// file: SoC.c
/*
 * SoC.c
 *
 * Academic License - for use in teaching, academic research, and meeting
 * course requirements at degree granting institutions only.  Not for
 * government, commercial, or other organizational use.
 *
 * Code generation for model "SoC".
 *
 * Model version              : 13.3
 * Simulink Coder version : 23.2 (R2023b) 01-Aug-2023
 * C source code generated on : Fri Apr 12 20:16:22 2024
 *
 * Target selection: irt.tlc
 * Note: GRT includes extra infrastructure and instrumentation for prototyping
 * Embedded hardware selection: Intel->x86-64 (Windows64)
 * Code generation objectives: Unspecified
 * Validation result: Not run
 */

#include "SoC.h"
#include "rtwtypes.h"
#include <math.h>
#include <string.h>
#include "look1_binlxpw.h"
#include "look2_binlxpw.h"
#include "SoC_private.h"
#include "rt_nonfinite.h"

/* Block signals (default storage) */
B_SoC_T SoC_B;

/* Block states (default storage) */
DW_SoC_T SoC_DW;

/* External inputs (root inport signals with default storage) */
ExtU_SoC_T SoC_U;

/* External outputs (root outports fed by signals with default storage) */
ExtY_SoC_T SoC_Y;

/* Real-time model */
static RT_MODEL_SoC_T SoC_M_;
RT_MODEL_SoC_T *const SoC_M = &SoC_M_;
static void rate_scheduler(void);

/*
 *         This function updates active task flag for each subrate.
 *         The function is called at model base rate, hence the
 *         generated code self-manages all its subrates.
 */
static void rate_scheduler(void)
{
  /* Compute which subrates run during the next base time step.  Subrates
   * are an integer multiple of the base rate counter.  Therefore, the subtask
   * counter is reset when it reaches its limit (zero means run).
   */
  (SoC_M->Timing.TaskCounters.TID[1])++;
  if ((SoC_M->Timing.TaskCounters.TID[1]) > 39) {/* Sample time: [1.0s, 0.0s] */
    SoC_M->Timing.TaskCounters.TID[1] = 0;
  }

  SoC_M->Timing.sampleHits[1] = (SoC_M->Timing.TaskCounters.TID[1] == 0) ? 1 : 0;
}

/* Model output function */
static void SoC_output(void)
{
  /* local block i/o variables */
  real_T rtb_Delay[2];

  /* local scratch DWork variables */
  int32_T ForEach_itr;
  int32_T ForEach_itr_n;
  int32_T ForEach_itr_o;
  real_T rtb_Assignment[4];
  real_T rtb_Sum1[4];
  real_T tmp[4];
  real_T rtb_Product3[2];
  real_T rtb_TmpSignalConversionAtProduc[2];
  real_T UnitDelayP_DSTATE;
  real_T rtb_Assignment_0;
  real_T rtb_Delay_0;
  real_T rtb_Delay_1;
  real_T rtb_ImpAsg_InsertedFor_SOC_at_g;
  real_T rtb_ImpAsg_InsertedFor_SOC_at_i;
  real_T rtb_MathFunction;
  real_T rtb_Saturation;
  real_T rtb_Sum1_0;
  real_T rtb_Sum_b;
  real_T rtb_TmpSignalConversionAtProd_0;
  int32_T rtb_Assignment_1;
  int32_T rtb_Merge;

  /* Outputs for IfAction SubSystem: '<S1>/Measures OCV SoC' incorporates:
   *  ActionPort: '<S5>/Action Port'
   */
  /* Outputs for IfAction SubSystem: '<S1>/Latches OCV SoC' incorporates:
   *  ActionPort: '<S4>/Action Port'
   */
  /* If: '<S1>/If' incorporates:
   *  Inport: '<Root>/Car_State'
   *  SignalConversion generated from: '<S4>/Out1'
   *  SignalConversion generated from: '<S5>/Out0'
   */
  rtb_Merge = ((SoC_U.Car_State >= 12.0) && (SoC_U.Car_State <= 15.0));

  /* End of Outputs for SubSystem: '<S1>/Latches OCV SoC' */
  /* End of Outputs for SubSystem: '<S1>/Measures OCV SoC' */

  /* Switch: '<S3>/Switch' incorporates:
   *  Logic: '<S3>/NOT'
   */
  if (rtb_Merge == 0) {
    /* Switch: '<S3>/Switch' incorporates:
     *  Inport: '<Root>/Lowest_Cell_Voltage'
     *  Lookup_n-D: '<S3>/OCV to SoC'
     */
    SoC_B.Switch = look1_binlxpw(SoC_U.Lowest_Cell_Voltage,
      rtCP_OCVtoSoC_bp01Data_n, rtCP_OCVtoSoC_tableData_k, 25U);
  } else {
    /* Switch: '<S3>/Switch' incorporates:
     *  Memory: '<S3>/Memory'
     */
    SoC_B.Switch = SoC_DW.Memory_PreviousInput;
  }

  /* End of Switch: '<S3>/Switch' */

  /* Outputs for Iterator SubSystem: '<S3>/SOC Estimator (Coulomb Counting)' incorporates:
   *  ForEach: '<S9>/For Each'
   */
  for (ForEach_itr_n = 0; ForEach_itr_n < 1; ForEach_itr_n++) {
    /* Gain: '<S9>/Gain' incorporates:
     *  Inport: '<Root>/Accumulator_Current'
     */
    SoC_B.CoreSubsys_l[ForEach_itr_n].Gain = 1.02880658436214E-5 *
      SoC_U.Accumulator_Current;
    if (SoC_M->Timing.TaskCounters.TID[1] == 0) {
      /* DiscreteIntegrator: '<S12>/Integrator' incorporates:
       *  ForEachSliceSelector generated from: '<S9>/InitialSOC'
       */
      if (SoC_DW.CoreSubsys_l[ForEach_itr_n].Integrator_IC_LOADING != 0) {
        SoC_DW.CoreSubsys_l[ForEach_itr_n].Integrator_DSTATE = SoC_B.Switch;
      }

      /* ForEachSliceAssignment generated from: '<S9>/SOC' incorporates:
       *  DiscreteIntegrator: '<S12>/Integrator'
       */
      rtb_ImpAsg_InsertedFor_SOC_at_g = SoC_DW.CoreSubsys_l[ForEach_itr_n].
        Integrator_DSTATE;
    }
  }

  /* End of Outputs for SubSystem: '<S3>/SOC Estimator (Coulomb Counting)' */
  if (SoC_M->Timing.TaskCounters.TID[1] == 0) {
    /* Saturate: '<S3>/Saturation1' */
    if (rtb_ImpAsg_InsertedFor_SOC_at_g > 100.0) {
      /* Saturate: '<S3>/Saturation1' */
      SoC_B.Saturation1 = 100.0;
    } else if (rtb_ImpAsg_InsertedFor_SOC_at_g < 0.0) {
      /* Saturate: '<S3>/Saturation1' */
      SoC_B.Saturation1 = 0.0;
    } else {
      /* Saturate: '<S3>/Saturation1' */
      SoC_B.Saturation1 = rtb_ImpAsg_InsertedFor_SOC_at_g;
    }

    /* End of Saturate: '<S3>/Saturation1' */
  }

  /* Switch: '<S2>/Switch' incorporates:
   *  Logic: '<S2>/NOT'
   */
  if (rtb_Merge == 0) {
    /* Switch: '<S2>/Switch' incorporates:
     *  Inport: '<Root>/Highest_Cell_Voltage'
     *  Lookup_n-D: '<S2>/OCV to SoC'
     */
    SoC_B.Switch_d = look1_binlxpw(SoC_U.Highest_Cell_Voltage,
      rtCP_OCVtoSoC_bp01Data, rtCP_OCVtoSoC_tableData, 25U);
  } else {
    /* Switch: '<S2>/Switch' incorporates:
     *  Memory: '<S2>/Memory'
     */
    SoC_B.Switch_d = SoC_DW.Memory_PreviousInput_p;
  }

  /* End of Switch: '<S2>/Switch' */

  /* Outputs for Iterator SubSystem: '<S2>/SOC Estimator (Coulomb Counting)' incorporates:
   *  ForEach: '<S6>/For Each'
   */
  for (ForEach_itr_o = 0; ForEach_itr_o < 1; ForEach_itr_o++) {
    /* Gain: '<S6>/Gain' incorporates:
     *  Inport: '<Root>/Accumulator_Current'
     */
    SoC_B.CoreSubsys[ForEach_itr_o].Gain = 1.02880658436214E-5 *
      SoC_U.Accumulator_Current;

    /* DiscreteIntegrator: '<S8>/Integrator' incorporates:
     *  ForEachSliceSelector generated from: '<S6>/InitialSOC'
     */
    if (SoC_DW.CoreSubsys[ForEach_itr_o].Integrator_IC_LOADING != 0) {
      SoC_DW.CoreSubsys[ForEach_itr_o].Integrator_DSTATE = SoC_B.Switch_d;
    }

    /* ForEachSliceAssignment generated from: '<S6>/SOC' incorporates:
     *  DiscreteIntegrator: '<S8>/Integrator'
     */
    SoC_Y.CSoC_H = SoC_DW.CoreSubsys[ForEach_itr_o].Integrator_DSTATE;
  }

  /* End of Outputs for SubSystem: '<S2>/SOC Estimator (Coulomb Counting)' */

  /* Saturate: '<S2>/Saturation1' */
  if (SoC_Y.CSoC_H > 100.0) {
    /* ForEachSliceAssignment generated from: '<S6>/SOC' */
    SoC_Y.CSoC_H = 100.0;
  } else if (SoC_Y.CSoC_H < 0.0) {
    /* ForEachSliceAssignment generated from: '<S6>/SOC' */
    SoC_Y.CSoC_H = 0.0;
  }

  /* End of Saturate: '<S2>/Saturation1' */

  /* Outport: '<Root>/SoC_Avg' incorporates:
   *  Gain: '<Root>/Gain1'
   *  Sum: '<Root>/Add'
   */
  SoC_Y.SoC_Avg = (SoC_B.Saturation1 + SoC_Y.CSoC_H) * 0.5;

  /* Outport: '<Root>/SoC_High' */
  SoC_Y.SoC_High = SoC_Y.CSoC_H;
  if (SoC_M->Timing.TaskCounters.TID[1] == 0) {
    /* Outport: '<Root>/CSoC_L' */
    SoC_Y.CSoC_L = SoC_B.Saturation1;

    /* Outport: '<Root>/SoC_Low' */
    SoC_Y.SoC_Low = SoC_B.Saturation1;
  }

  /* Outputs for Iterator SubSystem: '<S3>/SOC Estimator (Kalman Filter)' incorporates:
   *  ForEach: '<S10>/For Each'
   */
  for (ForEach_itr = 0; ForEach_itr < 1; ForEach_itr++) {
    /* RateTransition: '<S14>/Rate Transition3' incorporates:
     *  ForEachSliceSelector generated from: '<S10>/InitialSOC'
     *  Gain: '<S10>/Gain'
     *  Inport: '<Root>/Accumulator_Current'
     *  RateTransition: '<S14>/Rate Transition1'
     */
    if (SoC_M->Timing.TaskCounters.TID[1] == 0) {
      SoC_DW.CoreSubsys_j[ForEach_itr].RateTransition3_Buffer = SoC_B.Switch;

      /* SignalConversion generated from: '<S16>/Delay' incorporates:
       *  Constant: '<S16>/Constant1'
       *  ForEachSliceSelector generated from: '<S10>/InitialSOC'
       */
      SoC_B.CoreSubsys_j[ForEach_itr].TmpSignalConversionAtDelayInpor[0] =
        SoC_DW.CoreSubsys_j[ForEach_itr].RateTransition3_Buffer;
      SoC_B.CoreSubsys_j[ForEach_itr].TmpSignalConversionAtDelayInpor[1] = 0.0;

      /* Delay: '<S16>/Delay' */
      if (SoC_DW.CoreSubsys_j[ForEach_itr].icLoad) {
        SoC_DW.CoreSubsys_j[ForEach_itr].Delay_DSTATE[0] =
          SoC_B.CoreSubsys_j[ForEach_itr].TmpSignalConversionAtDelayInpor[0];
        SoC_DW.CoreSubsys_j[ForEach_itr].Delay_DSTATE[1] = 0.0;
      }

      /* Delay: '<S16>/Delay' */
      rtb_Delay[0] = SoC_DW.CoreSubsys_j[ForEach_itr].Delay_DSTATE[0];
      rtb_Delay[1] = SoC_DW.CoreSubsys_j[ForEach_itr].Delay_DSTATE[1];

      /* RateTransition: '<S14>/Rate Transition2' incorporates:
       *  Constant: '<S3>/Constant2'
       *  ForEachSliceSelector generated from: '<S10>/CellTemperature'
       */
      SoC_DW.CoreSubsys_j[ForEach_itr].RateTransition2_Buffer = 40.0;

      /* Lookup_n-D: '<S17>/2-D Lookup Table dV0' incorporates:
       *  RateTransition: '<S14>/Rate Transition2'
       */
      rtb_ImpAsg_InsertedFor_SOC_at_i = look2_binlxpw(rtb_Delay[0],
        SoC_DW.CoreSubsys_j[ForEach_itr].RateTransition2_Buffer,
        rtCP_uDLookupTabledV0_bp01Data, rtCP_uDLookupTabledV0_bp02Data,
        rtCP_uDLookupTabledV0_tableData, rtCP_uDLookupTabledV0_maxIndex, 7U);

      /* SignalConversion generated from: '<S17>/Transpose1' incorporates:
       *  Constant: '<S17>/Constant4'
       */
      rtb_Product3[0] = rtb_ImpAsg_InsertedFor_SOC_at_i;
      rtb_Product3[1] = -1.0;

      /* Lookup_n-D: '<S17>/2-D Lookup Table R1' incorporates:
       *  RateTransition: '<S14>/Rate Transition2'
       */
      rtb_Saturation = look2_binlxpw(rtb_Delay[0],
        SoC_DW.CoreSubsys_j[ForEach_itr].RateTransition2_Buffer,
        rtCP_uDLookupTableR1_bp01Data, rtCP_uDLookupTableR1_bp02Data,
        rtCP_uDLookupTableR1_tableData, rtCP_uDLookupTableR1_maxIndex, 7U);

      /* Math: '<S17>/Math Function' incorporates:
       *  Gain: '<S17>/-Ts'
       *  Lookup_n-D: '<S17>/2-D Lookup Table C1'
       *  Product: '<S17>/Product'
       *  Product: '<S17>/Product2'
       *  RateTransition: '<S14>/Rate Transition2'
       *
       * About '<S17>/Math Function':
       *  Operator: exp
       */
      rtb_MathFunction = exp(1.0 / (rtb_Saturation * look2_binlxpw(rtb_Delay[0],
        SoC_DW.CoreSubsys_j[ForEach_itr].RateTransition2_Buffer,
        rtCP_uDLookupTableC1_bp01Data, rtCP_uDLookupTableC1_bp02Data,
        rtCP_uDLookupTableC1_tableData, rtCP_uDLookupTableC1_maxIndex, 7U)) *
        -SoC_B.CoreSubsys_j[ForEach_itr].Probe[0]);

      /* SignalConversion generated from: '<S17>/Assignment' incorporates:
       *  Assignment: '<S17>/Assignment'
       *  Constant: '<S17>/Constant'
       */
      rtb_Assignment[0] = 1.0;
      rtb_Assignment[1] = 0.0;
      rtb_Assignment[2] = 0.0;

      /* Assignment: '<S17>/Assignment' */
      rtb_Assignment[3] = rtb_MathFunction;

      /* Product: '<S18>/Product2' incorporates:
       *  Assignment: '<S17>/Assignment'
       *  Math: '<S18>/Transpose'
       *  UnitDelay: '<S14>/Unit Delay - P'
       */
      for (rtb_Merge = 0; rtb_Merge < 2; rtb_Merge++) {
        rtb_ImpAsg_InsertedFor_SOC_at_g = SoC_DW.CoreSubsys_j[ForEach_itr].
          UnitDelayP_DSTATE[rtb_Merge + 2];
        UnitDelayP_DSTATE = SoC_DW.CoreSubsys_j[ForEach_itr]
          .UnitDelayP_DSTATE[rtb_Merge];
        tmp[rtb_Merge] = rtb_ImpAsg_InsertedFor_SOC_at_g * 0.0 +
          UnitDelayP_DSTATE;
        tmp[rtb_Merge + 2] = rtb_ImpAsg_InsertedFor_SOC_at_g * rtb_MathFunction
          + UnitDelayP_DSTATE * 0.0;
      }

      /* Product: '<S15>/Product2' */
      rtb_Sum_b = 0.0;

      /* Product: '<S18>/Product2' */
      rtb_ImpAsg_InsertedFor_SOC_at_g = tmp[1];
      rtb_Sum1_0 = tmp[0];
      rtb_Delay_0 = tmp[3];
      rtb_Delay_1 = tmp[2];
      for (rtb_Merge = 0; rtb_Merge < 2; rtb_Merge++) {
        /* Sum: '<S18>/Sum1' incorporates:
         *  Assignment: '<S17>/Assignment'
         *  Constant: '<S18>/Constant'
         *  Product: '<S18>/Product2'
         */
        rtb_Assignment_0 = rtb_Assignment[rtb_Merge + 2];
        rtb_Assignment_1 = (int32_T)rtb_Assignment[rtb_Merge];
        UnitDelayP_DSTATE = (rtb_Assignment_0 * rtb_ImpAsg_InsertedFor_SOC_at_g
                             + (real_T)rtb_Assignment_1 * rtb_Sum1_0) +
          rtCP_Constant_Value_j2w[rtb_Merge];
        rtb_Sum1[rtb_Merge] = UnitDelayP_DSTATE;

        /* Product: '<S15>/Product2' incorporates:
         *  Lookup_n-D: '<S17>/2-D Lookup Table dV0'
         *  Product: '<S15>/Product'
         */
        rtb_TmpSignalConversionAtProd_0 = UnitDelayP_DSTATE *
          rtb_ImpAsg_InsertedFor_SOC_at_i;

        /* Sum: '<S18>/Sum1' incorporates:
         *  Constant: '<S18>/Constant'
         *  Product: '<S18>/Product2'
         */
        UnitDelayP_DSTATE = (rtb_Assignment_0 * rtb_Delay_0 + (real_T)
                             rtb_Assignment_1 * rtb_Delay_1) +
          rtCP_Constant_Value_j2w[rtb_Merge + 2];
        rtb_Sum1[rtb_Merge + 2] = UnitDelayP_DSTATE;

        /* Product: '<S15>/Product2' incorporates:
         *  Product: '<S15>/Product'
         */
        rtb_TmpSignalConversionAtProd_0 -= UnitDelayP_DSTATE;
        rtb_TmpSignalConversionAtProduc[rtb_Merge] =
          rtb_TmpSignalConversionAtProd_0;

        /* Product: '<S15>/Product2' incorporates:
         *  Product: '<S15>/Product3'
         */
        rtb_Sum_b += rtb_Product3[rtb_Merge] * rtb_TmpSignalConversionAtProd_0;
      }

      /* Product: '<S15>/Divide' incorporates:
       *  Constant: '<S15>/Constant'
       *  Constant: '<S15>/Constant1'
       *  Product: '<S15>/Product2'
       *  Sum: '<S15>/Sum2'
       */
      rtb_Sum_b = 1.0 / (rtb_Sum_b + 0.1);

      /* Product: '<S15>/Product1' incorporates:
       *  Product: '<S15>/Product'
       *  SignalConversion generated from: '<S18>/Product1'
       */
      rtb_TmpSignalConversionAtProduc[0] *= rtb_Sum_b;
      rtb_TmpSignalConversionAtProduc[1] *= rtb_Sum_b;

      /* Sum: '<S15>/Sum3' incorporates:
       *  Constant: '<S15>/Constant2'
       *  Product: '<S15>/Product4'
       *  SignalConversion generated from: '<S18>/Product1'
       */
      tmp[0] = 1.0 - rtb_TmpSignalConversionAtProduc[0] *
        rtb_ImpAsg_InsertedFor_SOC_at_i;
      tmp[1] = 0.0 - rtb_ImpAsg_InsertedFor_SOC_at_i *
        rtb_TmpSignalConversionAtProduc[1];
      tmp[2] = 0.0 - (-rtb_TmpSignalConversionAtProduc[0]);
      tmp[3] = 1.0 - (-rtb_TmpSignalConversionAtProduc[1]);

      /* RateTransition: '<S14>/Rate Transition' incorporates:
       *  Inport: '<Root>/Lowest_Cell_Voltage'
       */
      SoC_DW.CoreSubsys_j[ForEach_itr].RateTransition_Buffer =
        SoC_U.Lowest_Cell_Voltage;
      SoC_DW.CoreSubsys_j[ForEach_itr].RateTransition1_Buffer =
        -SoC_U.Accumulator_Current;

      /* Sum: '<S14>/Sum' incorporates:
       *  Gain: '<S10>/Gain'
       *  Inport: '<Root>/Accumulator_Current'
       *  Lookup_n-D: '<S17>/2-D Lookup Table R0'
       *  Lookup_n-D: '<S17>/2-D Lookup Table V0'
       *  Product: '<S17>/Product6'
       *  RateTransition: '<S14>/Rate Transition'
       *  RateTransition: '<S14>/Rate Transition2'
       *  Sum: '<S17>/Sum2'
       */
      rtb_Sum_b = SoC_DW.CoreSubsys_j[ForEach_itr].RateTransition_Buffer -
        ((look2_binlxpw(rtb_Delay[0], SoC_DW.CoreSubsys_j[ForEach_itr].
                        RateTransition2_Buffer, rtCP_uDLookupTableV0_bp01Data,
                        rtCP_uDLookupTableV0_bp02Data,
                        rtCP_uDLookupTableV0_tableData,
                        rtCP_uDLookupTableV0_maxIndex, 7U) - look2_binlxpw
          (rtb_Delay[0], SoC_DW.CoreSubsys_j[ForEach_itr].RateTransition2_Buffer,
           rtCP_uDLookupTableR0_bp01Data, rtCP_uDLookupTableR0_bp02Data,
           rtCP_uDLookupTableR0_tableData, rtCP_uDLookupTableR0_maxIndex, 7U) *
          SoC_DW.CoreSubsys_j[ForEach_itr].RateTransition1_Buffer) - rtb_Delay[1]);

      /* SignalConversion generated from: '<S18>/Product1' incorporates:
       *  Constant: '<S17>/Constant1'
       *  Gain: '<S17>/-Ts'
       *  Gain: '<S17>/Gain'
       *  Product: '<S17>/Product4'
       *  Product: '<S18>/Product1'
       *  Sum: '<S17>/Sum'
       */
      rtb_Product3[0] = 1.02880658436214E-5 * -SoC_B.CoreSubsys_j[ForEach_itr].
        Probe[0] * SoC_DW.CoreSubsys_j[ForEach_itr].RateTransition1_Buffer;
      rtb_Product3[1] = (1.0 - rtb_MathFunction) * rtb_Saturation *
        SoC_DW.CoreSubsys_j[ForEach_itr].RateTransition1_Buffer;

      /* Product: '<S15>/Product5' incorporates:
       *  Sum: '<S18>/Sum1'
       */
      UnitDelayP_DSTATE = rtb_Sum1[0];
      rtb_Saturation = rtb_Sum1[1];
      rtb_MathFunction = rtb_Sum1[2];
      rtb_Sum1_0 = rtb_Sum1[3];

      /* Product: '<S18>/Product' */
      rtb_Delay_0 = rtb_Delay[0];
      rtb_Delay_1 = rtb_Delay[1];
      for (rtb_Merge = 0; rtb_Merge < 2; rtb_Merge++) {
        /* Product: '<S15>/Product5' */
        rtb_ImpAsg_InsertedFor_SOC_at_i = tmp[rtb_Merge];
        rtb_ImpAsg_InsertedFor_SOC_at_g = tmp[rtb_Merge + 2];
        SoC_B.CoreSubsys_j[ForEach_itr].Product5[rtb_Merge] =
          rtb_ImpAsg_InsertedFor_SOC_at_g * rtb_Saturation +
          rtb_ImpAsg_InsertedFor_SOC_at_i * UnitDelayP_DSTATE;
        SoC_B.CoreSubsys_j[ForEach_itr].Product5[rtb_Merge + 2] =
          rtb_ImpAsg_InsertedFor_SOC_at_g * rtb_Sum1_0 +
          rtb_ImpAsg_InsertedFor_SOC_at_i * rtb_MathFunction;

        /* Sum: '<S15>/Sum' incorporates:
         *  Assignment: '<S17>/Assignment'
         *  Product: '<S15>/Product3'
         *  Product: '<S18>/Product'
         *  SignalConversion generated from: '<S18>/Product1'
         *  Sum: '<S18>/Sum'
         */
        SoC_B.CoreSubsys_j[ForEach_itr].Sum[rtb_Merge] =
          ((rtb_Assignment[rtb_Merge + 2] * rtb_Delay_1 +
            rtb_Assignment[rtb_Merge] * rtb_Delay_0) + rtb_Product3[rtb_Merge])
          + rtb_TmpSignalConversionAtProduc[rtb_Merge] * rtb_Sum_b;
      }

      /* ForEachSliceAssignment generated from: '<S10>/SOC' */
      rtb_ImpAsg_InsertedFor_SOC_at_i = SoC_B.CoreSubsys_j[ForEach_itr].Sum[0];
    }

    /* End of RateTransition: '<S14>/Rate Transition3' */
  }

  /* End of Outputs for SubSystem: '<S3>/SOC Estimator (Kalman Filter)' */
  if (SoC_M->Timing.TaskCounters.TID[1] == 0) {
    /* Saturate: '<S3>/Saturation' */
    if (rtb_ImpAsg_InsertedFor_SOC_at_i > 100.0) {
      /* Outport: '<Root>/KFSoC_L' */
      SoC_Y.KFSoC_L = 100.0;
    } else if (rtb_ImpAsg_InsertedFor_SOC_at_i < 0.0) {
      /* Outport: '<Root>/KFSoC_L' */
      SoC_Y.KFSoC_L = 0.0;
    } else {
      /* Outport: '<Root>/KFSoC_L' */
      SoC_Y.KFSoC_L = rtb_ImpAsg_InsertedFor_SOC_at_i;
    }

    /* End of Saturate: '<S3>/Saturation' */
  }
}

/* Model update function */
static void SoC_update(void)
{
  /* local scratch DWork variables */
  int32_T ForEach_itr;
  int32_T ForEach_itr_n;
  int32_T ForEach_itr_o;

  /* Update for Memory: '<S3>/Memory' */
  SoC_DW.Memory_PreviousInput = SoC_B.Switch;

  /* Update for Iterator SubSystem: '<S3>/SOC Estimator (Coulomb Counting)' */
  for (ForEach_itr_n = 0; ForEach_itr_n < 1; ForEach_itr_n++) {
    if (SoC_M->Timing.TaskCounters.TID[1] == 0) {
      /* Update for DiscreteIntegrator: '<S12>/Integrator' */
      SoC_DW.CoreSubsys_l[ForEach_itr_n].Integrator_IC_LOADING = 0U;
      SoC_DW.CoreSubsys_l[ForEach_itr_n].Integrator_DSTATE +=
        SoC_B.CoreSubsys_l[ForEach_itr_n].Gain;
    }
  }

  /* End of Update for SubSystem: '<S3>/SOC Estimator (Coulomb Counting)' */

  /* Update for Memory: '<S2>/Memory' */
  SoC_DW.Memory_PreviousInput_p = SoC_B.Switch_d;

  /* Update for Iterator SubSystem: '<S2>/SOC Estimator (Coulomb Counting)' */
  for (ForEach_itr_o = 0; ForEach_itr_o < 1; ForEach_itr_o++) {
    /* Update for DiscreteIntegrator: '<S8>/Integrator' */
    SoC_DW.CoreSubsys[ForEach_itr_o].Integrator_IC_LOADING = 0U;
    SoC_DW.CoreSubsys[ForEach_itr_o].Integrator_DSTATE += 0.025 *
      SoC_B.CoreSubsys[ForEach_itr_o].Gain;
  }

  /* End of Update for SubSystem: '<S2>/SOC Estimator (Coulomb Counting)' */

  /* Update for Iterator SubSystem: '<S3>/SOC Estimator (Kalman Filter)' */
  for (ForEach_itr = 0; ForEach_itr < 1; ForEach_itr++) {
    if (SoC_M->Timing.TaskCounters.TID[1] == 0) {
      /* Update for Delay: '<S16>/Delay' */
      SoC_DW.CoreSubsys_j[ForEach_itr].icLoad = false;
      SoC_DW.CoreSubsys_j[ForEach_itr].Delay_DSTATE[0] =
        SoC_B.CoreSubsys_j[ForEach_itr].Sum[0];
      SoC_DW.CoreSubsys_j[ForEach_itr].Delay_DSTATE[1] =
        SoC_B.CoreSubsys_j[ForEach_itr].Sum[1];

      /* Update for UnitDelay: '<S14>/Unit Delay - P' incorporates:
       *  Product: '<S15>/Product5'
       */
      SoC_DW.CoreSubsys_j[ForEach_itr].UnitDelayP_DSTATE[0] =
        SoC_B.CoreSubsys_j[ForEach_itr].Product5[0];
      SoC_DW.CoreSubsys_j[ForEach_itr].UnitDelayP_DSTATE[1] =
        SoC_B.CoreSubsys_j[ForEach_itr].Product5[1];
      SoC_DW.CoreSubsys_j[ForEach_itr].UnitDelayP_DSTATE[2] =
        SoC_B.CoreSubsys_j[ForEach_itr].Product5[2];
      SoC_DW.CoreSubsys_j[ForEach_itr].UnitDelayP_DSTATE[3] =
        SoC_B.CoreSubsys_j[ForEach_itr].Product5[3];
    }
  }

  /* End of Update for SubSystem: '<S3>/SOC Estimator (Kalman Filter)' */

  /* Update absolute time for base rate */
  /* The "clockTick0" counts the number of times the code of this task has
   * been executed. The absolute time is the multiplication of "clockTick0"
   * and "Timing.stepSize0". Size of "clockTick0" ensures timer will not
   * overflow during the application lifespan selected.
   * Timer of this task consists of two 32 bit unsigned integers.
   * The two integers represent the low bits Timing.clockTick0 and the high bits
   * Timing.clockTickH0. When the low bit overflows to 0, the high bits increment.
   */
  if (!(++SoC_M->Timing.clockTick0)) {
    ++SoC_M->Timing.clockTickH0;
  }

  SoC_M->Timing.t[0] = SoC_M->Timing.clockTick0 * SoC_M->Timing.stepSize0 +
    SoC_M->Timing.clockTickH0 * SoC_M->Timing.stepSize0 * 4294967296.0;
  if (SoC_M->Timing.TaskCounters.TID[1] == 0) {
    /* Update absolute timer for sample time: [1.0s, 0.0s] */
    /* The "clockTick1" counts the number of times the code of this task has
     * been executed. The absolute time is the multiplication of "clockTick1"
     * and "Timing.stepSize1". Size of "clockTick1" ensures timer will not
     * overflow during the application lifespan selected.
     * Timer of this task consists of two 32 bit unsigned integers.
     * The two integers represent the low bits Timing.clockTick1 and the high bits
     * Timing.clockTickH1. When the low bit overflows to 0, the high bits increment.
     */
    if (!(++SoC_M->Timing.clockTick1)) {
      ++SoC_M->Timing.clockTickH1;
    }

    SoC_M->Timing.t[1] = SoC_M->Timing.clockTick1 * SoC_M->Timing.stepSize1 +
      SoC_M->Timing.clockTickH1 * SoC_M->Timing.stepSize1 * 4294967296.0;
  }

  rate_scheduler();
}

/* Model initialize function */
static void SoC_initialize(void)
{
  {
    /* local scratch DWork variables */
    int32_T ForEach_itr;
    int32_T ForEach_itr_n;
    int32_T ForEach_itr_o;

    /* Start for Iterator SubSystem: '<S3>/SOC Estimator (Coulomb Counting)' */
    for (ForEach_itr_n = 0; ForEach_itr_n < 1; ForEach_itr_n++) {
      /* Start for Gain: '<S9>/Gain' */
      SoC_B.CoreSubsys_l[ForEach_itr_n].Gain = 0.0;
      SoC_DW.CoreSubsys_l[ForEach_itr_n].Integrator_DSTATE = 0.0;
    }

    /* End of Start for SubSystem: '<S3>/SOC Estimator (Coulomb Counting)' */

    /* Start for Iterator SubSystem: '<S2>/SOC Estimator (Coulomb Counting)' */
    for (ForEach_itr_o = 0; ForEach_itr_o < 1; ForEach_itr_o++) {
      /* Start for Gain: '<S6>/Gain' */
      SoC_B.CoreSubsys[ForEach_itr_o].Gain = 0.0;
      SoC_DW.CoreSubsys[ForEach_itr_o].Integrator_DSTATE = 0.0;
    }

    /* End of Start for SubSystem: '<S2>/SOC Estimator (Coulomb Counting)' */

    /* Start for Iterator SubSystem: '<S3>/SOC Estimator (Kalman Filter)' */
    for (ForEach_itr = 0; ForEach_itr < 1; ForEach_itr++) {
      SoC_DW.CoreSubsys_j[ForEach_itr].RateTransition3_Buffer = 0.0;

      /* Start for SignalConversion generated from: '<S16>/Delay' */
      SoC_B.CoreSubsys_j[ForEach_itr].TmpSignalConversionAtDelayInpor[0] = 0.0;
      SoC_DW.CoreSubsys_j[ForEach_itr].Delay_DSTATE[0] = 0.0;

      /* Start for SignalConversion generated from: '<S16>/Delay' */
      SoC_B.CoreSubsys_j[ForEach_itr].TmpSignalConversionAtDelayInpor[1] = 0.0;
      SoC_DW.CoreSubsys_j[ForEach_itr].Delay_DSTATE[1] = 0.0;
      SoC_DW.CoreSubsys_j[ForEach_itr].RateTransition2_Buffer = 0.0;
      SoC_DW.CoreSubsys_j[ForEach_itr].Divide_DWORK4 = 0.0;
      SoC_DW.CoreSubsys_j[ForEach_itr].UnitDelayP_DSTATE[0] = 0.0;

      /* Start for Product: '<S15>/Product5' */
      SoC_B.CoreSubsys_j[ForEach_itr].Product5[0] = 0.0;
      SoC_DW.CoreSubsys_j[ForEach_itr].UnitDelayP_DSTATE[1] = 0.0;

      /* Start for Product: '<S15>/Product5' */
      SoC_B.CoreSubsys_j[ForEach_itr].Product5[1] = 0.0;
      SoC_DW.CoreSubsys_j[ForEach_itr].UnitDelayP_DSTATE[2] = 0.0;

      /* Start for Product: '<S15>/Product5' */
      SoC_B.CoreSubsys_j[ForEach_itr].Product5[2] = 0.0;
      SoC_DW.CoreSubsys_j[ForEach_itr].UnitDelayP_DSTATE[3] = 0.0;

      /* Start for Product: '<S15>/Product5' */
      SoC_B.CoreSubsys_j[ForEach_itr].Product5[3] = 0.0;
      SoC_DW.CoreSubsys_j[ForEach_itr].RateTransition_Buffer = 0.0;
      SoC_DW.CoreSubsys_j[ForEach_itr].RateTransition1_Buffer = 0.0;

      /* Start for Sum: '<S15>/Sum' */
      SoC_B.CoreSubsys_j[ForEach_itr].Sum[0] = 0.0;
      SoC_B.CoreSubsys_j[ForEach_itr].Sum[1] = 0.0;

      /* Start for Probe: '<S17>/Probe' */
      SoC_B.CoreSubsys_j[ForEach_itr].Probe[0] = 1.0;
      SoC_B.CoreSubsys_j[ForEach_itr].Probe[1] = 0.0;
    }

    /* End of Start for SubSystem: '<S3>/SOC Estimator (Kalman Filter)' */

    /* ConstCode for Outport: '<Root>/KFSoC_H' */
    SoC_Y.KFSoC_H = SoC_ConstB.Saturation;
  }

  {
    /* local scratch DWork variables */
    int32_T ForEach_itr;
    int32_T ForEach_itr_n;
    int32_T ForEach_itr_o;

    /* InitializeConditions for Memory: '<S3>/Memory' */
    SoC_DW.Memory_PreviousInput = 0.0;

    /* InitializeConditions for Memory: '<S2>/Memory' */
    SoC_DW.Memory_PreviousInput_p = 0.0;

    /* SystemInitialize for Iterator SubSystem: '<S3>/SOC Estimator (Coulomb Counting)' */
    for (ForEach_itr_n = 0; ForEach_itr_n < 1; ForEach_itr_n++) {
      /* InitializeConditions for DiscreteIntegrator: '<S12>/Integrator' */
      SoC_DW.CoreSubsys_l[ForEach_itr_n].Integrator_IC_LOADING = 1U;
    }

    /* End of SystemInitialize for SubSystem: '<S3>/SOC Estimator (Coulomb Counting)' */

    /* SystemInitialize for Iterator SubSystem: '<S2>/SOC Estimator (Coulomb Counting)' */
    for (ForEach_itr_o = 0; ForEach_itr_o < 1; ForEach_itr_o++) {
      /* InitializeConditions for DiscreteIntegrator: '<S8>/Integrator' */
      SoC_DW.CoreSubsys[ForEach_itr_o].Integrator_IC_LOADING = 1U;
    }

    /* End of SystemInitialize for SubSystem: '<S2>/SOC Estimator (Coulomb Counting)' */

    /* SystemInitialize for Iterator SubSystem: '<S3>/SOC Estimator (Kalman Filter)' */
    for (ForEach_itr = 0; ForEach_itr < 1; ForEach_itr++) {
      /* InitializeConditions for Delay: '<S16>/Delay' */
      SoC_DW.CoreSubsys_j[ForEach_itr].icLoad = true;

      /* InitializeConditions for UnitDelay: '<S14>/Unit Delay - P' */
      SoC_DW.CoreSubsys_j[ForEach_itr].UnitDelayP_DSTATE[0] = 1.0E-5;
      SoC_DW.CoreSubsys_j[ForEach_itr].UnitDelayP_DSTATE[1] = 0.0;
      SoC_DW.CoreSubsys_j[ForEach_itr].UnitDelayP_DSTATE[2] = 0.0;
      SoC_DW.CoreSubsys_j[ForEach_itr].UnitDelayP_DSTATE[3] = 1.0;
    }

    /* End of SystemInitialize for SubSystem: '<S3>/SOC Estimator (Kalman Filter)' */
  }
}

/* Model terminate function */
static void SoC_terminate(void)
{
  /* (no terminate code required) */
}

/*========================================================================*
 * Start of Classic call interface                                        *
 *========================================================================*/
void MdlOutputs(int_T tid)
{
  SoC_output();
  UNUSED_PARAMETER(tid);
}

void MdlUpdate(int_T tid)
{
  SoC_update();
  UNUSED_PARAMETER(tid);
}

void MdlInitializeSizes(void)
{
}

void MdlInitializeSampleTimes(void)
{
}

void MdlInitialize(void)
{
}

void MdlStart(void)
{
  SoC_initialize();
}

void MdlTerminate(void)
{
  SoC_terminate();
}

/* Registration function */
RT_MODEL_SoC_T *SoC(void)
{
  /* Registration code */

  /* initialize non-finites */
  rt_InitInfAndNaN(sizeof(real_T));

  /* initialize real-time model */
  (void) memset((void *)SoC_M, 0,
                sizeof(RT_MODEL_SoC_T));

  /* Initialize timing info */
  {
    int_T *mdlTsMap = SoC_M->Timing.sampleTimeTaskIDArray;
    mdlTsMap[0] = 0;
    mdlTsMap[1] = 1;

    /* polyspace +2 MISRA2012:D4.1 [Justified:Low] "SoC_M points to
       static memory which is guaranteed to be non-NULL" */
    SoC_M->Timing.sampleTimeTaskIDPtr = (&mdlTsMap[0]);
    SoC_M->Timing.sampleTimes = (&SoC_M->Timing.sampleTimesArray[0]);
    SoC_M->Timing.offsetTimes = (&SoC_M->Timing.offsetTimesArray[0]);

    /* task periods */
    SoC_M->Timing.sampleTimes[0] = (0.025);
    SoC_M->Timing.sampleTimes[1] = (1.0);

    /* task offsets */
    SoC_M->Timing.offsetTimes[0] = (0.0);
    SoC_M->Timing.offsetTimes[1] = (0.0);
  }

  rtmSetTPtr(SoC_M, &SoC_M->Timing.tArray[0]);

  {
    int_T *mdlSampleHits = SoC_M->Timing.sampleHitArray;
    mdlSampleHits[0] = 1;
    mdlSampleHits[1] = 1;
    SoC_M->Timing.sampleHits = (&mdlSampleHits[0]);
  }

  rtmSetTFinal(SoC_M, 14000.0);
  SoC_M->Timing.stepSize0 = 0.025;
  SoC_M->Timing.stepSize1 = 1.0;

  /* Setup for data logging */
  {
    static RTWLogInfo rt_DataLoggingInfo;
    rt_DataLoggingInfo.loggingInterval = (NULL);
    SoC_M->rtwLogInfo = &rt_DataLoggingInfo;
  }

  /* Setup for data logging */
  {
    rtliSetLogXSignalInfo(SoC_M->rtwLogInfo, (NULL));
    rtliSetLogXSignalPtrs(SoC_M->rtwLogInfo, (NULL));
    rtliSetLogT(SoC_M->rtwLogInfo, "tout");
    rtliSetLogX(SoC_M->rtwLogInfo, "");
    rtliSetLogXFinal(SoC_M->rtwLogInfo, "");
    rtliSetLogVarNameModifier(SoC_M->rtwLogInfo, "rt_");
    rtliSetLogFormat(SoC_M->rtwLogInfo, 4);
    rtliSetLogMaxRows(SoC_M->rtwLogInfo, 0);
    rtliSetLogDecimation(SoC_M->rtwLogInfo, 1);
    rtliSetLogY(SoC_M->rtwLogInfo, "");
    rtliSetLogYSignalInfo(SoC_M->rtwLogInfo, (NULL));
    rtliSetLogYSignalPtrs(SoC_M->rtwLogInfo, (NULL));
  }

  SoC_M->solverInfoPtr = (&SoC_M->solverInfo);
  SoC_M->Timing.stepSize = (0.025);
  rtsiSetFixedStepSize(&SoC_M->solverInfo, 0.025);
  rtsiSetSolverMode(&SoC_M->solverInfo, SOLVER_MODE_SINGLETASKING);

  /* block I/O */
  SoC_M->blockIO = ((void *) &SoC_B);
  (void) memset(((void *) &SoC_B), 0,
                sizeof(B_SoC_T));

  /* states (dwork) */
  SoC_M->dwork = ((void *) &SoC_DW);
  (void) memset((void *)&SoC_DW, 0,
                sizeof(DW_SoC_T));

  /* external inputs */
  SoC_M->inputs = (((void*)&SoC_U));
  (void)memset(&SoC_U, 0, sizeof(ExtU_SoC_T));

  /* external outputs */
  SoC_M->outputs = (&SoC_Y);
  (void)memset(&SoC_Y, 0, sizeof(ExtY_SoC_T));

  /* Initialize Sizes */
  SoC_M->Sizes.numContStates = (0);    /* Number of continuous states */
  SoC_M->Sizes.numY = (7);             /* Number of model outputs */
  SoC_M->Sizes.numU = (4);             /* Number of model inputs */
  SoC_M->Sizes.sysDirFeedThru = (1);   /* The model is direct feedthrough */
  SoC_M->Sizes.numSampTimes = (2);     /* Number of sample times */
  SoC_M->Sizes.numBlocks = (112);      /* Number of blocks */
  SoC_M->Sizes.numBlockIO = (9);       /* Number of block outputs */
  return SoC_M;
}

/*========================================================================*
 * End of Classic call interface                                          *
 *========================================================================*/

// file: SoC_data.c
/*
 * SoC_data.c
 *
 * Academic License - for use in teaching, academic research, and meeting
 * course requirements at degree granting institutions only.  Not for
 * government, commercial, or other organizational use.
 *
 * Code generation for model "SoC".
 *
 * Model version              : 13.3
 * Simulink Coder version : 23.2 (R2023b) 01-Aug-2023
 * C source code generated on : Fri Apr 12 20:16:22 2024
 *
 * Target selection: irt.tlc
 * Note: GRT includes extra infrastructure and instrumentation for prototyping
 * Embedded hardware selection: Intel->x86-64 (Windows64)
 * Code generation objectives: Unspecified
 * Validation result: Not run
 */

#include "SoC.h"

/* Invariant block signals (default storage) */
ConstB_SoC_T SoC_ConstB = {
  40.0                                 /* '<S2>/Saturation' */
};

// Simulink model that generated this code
simulink model "SoC"  (R2023b)
settings: Solver=FixedStepAuto  StartTime=0.0  StopTime=14000  RelTol=1e-3
libraries: BatteryEstimators x4

== system SoC ==
  Lowest_Cell_Voltage : Inport
  Highest_Cell_Voltage : Inport  Port=2
  Accumulator_Current : Inport  Port=3
  Car_State : Inport  Port=4
  Add : Sum
  Gain1 : Gain  Gain=0.5
  Init_SoC_Trigger value : Subsystem
  Manual Switch : ManualSwitch
  Manual Switch1 : ManualSwitch
  SoC_Highest : Subsystem
  SoC_Lowest : Subsystem
  SoC_Avg : Outport
  CSoC_L : Outport  Port=2
  KFSoC_L : Outport  Port=3
  CSoC_H : Outport  Port=4
  KFSoC_H : Outport  Port=5
  SoC_Low : Outport  Port=6
  SoC_High : Outport  Port=7
  wires:
  Lowest_Cell_Voltage/1 -> SoC_Lowest/2(V)
  Init_SoC_Trigger value/1(Init_SoC_Trigger) -> SoC_Highest/3(SoC_init_trigger), SoC_Lowest/3(SoC_init_trigger)
  Accumulator_Current/1 -> SoC_Highest/1(I), SoC_Lowest/1(I)
  SoC_Lowest/1(SoC_Coulomb) -> CSoC_L/1, Manual Switch/1
  SoC_Lowest/2(SoC_KF) -> KFSoC_L/1, Manual Switch/2
  SoC_Highest/2(SoC_KF) -> KFSoC_H/1, Manual Switch1/2
  SoC_Highest/1(SoC_Coulomb) -> CSoC_H/1, Manual Switch1/1
  Manual Switch/1 -> SoC_Low/1, Add/1
  Manual Switch1/1 -> SoC_High/1, Add/2
  Add/1 -> Gain1/1
  Gain1/1 -> SoC_Avg/1
  Highest_Cell_Voltage/1 -> SoC_Highest/2(V)
  Car_State/1 -> Init_SoC_Trigger value/1(Car_State)

== system SoC/Init_SoC_Trigger value ==
  Car_State : Inport
  If : If  IfExpression=u1 >= 12 & u1 <= 15
  Latches OCV SoC : Subsystem  TreatAsAtomicUnit=on
  Measures OCV SoC : Subsystem  TreatAsAtomicUnit=on
  Merge : Merge
  Init_SoC_Trigger : Outport  VectorParamsAs1DForOutWhenUnconnected=off
  wires:
  Car_State/1 -> If/1
  If/1 -> Latches OCV SoC/Action
  If/2 -> Measures OCV SoC/Action
  Measures OCV SoC/1(Out0) -> Merge/2
  Latches OCV SoC/1(Out1) -> Merge/1
  Merge/1 -> Init_SoC_Trigger/1

== system SoC/SoC_Highest ==
  I : Inport
  V : Inport  Port=2
  SoC_init_trigger : Inport  Port=3
  Constant1 : Constant  Value=40
  Memory : Memory
  NOT : Logic  Operator=NOT  IconShape=distinctive  AllPortsSameDT=off  OutDataTypeStr=boolean
  OCV to SoC : Lookup_n-D  NumberOfTableDimensions=1  BreakpointsForDimension1=|  Table=|  InternalRulePriority=Speed  RndMeth=Simplest
      BreakpointsForDimension1=|
      | [2.94959022892031
      | 3.21416977318498
      | 3.34338141328538
      | 3.38823547157865
      | 3.42107134634789
      | 3.48650481123582
      | 3.51335866761468
      | 3.54070339538832
      | 3.56968305677313
      | 3.63185877907628
      | 3.63255716896237
      | 3.64803371545993
      | 3.66548496788278
      | 3.66563518858557
      | 3.72681148156897
      | 3.76406010705888
      | 3.77075982343748
      | 3.84270466053206
      | 3.84295206305238
      | 3.90164564850831
      | 3.96498508551296
      | 3.96615700649565
      | 4.04797311953080
      | 4.07602027520885
      | 4.10936207844059
      | 4.18278376875771]
      Table=|
      | [0.00364887820512694
      | 0.0406322115384605
      | 0.0806891025641018
      | 0.120744391025641
      | 0.160802083333333
      | 0.200854967948718
      | 0.240911057692307
      | 0.280964743589743
      | 0.321025641025641
      | 0.361079326923077
      | 0.401137019230769
      | 0.441193910256410
      | 0.481247596153846
      | 0.521301282051282
      | 0.561357371794872
      | 0.601413461538462
      | 0.641456730769231
      | 0.681509615384616
      | 0.721566506410257
      | 0.761620993589744
      | 0.801677884615385
      | 0.841734775641026
      | 0.881788461538462
      | 0.921837339743590
      | 0.961899038461539
      | 0.998685256410256]
  SOC Estimator (Coulomb Counting) : BatteryEstimators/SOC Estimator (Coulomb Counting)  CurrentInputPartition=on  AH=2.6*5  Ts=1
  SOC Estimator (Kalman Filter) : BatteryEstimators/SOC Estimator (Kalman Filter)  CurrentInputPartition=off  filterType=Unscented Kalman filter  alpha=1  beta=2  kappa=0  Q=|  R=1e-3  P0=[1e-8 0; 0 1]  Ts=.025  SOC_vec=|  T_vec=[40+273]  R0_mat=|  R1_mat=|  tau1_mat=|  V0_mat=|  AH=12.5
      Q=|
      | [1e-9 0;
      | 0 1e-9]
      SOC_vec=|
      | [0.00364887820512694
      | 0.0406322115384605
      | 0.0806891025641018
      | 0.120744391025641
      | 0.160802083333333
      | 0.200854967948718
      | 0.240911057692307
      | 0.280964743589743
      | 0.321025641025641
      | 0.361079326923077
      | 0.401137019230769
      | 0.441193910256410
      | 0.481247596153846
      | 0.521301282051282
      | 0.561357371794872
      | 0.601413461538462
      | 0.641456730769231
      | 0.681509615384616
      | 0.721566506410257
      | 0.761620993589744
      | 0.801677884615385
      | 0.841734775641026
      | 0.881788461538462
      | 0.921837339743590
      | 0.961899038461539
      | 0.998685256410256]
      R0_mat=|
      | [0.0100233572019649
      | 0.0262776800968641
      | 0.0363128958641671
      | 0.0100113094505490
      | 0.0286486807277356
      | 0.0149767890889632
      | 0.0144578183036739
      | 0.0281525249750630
      | 0.0100063258437773
      | 0.0279749794813750
      | 0.0217631517067980
      | 0.0101315932150831
      | 0.0204969050806245
      | 0.0100036904397663
      | 0.0234196819492359
      | 0.0285785961250009
      | 0.0100010777636376
      | 0.0285512087508609
      | 0.0138948165245514
      | 0.0152455499563035
      | 0.0271834062533151
      | 0.00999543636151631
      | 0.0233190816650244
      | 0.0174459063712128
      | 0.00997795030699019
      | 0.0103822437854372]
      R1_mat=|
      | [0.000499569519126077
      | 0.000566384348175598
      | 0.000620513515330880
      | 0.000501834816986178
      | 0.000588952675343360
      | 0.000529656285954493
      | 0.000517421423028936
      | 0.000587687483006353
      | 0.000500912051109555
      | 0.000578364620913254
      | 0.000558041081149625
      | 0.000501034112890869
      | 0.000552539389402844
      | 0.000501551598015617
      | 0.000557375879673445
      | 0.000589089399714461
      | 0.000500612734241474
      | 0.000591500744740345
      | 0.000524954003879735
      | 0.000521737226573142
      | 0.000584978563699472
      | 0.000501333485097591
      | 0.000556455598375632
      | 0.000536187820761028
      | 0.000499639620215416
      | 0.000507199196258293]
      tau1_mat=|
      | [9.99999965128907
      | 9.98553115975498
      | 9.98319684629733
      | 9.99994867285566
      | 9.97472406054001
      | 9.99688938669185
      | 9.99522470508715
      | 9.98942560461659
      | 9.99999050049701
      | 9.99099110217109
      | 9.99738841102412
      | 9.99884730510879
      | 9.99441213972015
      | 9.99999487663704
      | 9.99510659168373
      | 9.99771333296480
      | 9.99992313725565
      | 9.99397201956115
      | 10.0015797566463
      | 9.99642521143648
      | 9.99339019420605
      | 9.99998885830201
      | 9.98301776831365
      | 9.99305327108613
      | 9.99970822142190
      | 9.99116677405533]
      V0_mat=|
      | [2.94959022892031
      | 3.21416977318498
      | 3.34338141328538
      | 3.38823547157865
      | 3.50107134634789
      | 3.48650481123582
      | 3.51335866761468
      | 3.58070339538832
      | 3.56968305677313
      | 3.63985877907628
      | 3.63255716896237
      | 3.62803371545993
      | 3.67548496788278
      | 3.66563518858557
      | 3.72681148156897
      | 3.76466010705888
      | 3.76075982343748
      | 3.85370466053206
      | 3.84295206305238
      | 3.90164564850831
      | 3.96498508551296
      | 3.96615700649565
      | 4.04797311953080
      | 4.07602027520885
      | 4.10936207844059
      | 4.18278376875771]
      link override Kalman Filter/EKBF/Jacobian/2-D Lookup Table C1: NumberOfTableDimensions=1
      link override Kalman Filter/EKBF/Jacobian/2-D Lookup Table R0: NumberOfTableDimensions=1
      link override Kalman Filter/EKBF/Jacobian/2-D Lookup Table R1: NumberOfTableDimensions=1
      link override Kalman Filter/EKBF/Jacobian/2-D Lookup Table V0: NumberOfTableDimensions=1
      link override Kalman Filter/EKBF/Jacobian/2-D Lookup Table dV0: NumberOfTableDimensions=1
      link override Kalman Filter/EKF/Jacobian/2-D Lookup Table C1: NumberOfTableDimensions=1
      link override Kalman Filter/EKF/Jacobian/2-D Lookup Table R0: NumberOfTableDimensions=1
      link override Kalman Filter/EKF/Jacobian/2-D Lookup Table R1: NumberOfTableDimensions=1
      link override Kalman Filter/EKF/Jacobian/2-D Lookup Table V0: NumberOfTableDimensions=1
      link override Kalman Filter/EKF/Jacobian/2-D Lookup Table dV0: NumberOfTableDimensions=1
      link override Kalman Filter/UKBF/Prediction-correction/Measurement function/Measurement function/OCV Table: NumberOfTableDimensions=1
      link override Kalman Filter/UKBF/Prediction-correction/Measurement function/Measurement function/R0 Table: NumberOfTableDimensions=1
      link override Kalman Filter/UKBF/Prediction-correction/State function/State function/C1: NumberOfTableDimensions=1
      link override Kalman Filter/UKBF/Prediction-correction/State function/State function/R1: NumberOfTableDimensions=1
      link override Kalman Filter/UKF/Prediction/Measurement function/Measurement function/OCV Table: NumberOfTableDimensions=1
      link override Kalman Filter/UKF/Prediction/Measurement function/Measurement function/R0 Table: NumberOfTableDimensions=1
      link override Kalman Filter/UKF/Prediction/State function/State function/C1: NumberOfTableDimensions=1
      link override Kalman Filter/UKF/Prediction/State function/State function/R1: NumberOfTableDimensions=1
  Saturation : Saturate  UpperLimit=100  LowerLimit=0
  Saturation1 : Saturate  UpperLimit=100  LowerLimit=0
  Switch : Switch  Criteria=u2 > Threshold  ZeroCross=off  SaturateOnIntegerOverflow=off  InputSameDT=off
  SoC_Coulomb : Outport  VectorParamsAs1DForOutWhenUnconnected=off
  SoC_KF : Outport  Port=2
  wires:
  Saturation1/1 -> SoC_Coulomb/1
  Saturation/1 -> SoC_KF/1
  SoC_init_trigger/1 -> NOT/1
  NOT/1 -> Switch/2
  Memory/1 -> Switch/3
  OCV to SoC/1 -> Switch/1
  V/1 -> SOC Estimator (Kalman Filter)/2, OCV to SoC/1
  Switch/1 -> SOC Estimator (Coulomb Counting)/2, SOC Estimator (Kalman Filter)/4, Memory/1
  I/1 -> SOC Estimator (Kalman Filter)/1, SOC Estimator (Coulomb Counting)/1
  Constant1/1 -> SOC Estimator (Kalman Filter)/3
  SOC Estimator (Kalman Filter)/1 -> Saturation/1  "Estimated SOC"
  SOC Estimator (Coulomb Counting)/1 -> Saturation1/1

== system SoC/SoC_Lowest ==
  I : Inport
  V : Inport  Port=2
  SoC_init_trigger : Inport  Port=3
  Constant1 : Constant  Value=40
  Memory : Memory
  NOT : Logic  Operator=NOT  IconShape=distinctive  AllPortsSameDT=off  OutDataTypeStr=boolean
  OCV to SoC : Lookup_n-D  NumberOfTableDimensions=1  BreakpointsForDimension1=|  Table=|  InternalRulePriority=Speed  RndMeth=Simplest
      BreakpointsForDimension1=|
      | [2.94959022892031
      | 3.21416977318498
      | 3.34338141328538
      | 3.38823547157865
      | 3.42107134634789
      | 3.48650481123582
      | 3.51335866761468
      | 3.54070339538832
      | 3.56968305677313
      | 3.63185877907628
      | 3.63255716896237
      | 3.64803371545993
      | 3.66548496788278
      | 3.66563518858557
      | 3.72681148156897
      | 3.76406010705888
      | 3.77075982343748
      | 3.84270466053206
      | 3.84295206305238
      | 3.90164564850831
      | 3.96498508551296
      | 3.96615700649565
      | 4.04797311953080
      | 4.07602027520885
      | 4.10936207844059
      | 4.18278376875771]
      Table=|
      | [0.00364887820512694
      | 0.0406322115384605
      | 0.0806891025641018
      | 0.120744391025641
      | 0.160802083333333
      | 0.200854967948718
      | 0.240911057692307
      | 0.280964743589743
      | 0.321025641025641
      | 0.361079326923077
      | 0.401137019230769
      | 0.441193910256410
      | 0.481247596153846
      | 0.521301282051282
      | 0.561357371794872
      | 0.601413461538462
      | 0.641456730769231
      | 0.681509615384616
      | 0.721566506410257
      | 0.761620993589744
      | 0.801677884615385
      | 0.841734775641026
      | 0.881788461538462
      | 0.921837339743590
      | 0.961899038461539
      | 0.998685256410256]
  SOC Estimator (Coulomb Counting) : BatteryEstimators/SOC Estimator (Coulomb Counting)  CurrentInputPartition=on  AH=2.6*5  Ts=1
  SOC Estimator (Kalman Filter) : BatteryEstimators/SOC Estimator (Kalman Filter)  CurrentInputPartition=off  filterType=Extended Kalman filter  alpha=1  beta=2  kappa=0  Q=|  R=1e-3  P0=[1e-8 0; 0 1]  Ts=.025  SOC_vec=|  T_vec=[40+273]  R0_mat=|  R1_mat=|  tau1_mat=|  V0_mat=|  AH=12.5
      Q=|
      | [1e-9 0;
      | 0 1e-9]
      SOC_vec=|
      | [0.00364887820512694
      | 0.0406322115384605
      | 0.0806891025641018
      | 0.120744391025641
      | 0.160802083333333
      | 0.200854967948718
      | 0.240911057692307
      | 0.280964743589743
      | 0.321025641025641
      | 0.361079326923077
      | 0.401137019230769
      | 0.441193910256410
      | 0.481247596153846
      | 0.521301282051282
      | 0.561357371794872
      | 0.601413461538462
      | 0.641456730769231
      | 0.681509615384616
      | 0.721566506410257
      | 0.761620993589744
      | 0.801677884615385
      | 0.841734775641026
      | 0.881788461538462
      | 0.921837339743590
      | 0.961899038461539
      | 0.998685256410256]
      R0_mat=|
      | [0.0100233572019649
      | 0.0262776800968641
      | 0.0363128958641671
      | 0.0100113094505490
      | 0.0286486807277356
      | 0.0149767890889632
      | 0.0144578183036739
      | 0.0281525249750630
      | 0.0100063258437773
      | 0.0279749794813750
      | 0.0217631517067980
      | 0.0101315932150831
      | 0.0204969050806245
      | 0.0100036904397663
      | 0.0234196819492359
      | 0.0285785961250009
      | 0.0100010777636376
      | 0.0285512087508609
      | 0.0138948165245514
      | 0.0152455499563035
      | 0.0271834062533151
      | 0.00999543636151631
      | 0.0233190816650244
      | 0.0174459063712128
      | 0.00997795030699019
      | 0.0103822437854372]
      R1_mat=|
      | [0.000499569519126077
      | 0.000566384348175598
      | 0.000620513515330880
      | 0.000501834816986178
      | 0.000588952675343360
      | 0.000529656285954493
      | 0.000517421423028936
      | 0.000587687483006353
      | 0.000500912051109555
      | 0.000578364620913254
      | 0.000558041081149625
      | 0.000501034112890869
      | 0.000552539389402844
      | 0.000501551598015617
      | 0.000557375879673445
      | 0.000589089399714461
      | 0.000500612734241474
      | 0.000591500744740345
      | 0.000524954003879735
      | 0.000521737226573142
      | 0.000584978563699472
      | 0.000501333485097591
      | 0.000556455598375632
      | 0.000536187820761028
      | 0.000499639620215416
      | 0.000507199196258293]
      tau1_mat=|
      | [9.99999965128907
      | 9.98553115975498
      | 9.98319684629733
      | 9.99994867285566
      | 9.97472406054001
      | 9.99688938669185
      | 9.99522470508715
      | 9.98942560461659
      | 9.99999050049701
      | 9.99099110217109
      | 9.99738841102412
      | 9.99884730510879
      | 9.99441213972015
      | 9.99999487663704
      | 9.99510659168373
      | 9.99771333296480
      | 9.99992313725565
      | 9.99397201956115
      | 10.0015797566463
      | 9.99642521143648
      | 9.99339019420605
      | 9.99998885830201
      | 9.98301776831365
      | 9.99305327108613
      | 9.99970822142190
      | 9.99116677405533]
      V0_mat=|
      | [2.94959022892031
      | 3.21416977318498
      | 3.34338141328538
      | 3.38823547157865
      | 3.50107134634789
      | 3.48650481123582
      | 3.51335866761468
      | 3.58070339538832
      | 3.56968305677313
      | 3.63985877907628
      | 3.63255716896237
      | 3.62803371545993
      | 3.67548496788278
      | 3.66563518858557
      | 3.72681148156897
      | 3.76466010705888
      | 3.76075982343748
      | 3.85370466053206
      | 3.84295206305238
      | 3.90164564850831
      | 3.96498508551296
      | 3.96615700649565
      | 4.04797311953080
      | 4.07602027520885
      | 4.10936207844059
      | 4.18278376875771]
      link override Kalman Filter/EKBF/Jacobian/2-D Lookup Table C1: NumberOfTableDimensions=1
      link override Kalman Filter/EKBF/Jacobian/2-D Lookup Table R0: NumberOfTableDimensions=1
      link override Kalman Filter/EKBF/Jacobian/2-D Lookup Table R1: NumberOfTableDimensions=1
      link override Kalman Filter/EKBF/Jacobian/2-D Lookup Table V0: NumberOfTableDimensions=1
      link override Kalman Filter/EKBF/Jacobian/2-D Lookup Table dV0: NumberOfTableDimensions=1
      link override Kalman Filter/EKF/Jacobian/2-D Lookup Table C1: NumberOfTableDimensions=1
      link override Kalman Filter/EKF/Jacobian/2-D Lookup Table R0: NumberOfTableDimensions=1
      link override Kalman Filter/EKF/Jacobian/2-D Lookup Table R1: NumberOfTableDimensions=1
      link override Kalman Filter/EKF/Jacobian/2-D Lookup Table V0: NumberOfTableDimensions=1
      link override Kalman Filter/EKF/Jacobian/2-D Lookup Table dV0: NumberOfTableDimensions=1
      link override Kalman Filter/UKBF/Prediction-correction/Measurement function/Measurement function/OCV Table: NumberOfTableDimensions=1
      link override Kalman Filter/UKBF/Prediction-correction/Measurement function/Measurement function/R0 Table: NumberOfTableDimensions=1
      link override Kalman Filter/UKBF/Prediction-correction/State function/State function/C1: NumberOfTableDimensions=1
      link override Kalman Filter/UKBF/Prediction-correction/State function/State function/R1: NumberOfTableDimensions=1
      link override Kalman Filter/UKF/Prediction/Measurement function/Measurement function/OCV Table: NumberOfTableDimensions=1
      link override Kalman Filter/UKF/Prediction/Measurement function/Measurement function/R0 Table: NumberOfTableDimensions=1
      link override Kalman Filter/UKF/Prediction/State function/State function/C1: NumberOfTableDimensions=1
      link override Kalman Filter/UKF/Prediction/State function/State function/R1: NumberOfTableDimensions=1
  Saturation : Saturate  UpperLimit=100  LowerLimit=0
  Saturation1 : Saturate  UpperLimit=100  LowerLimit=0
  Switch : Switch  Criteria=u2 > Threshold  ZeroCross=off  SaturateOnIntegerOverflow=off  InputSameDT=off
  SoC_Coulomb : Outport  VectorParamsAs1DForOutWhenUnconnected=off
  SoC_KF : Outport  Port=2
  wires:
  SOC Estimator (Coulomb Counting)/1 -> Saturation1/1
  SOC Estimator (Kalman Filter)/1 -> Saturation/1  "Estimated SOC"
  Constant1/1 -> SOC Estimator (Kalman Filter)/3
  I/1 -> SOC Estimator (Coulomb Counting)/1, SOC Estimator (Kalman Filter)/1
  Switch/1 -> Memory/1, SOC Estimator (Kalman Filter)/4, SOC Estimator (Coulomb Counting)/2
  V/1 -> OCV to SoC/1, SOC Estimator (Kalman Filter)/2
  OCV to SoC/1 -> Switch/1
  Memory/1 -> Switch/3
  NOT/1 -> Switch/2
  SoC_init_trigger/1 -> NOT/1
  Saturation/1 -> SoC_KF/1
  Saturation1/1 -> SoC_Coulomb/1

== system SoC/Init_SoC_Trigger value/Latches OCV SoC ==
  Action Port : ActionPort  ActionPortLabel=if(u1 >= 12 & u1 <= 15)
  Constant : Constant
  Out1 : Outport  VectorParamsAs1DForOutWhenUnconnected=off
  wires:
  Constant/1 -> Out1/1

== system SoC/Init_SoC_Trigger value/Measures OCV SoC ==
  Action Port : ActionPort  ActionPortLabel=else
  Constant : Constant  Value=0
  Out0 : Outport  VectorParamsAs1DForOutWhenUnconnected=off
  wires:
  Constant/1 -> Out0/1
